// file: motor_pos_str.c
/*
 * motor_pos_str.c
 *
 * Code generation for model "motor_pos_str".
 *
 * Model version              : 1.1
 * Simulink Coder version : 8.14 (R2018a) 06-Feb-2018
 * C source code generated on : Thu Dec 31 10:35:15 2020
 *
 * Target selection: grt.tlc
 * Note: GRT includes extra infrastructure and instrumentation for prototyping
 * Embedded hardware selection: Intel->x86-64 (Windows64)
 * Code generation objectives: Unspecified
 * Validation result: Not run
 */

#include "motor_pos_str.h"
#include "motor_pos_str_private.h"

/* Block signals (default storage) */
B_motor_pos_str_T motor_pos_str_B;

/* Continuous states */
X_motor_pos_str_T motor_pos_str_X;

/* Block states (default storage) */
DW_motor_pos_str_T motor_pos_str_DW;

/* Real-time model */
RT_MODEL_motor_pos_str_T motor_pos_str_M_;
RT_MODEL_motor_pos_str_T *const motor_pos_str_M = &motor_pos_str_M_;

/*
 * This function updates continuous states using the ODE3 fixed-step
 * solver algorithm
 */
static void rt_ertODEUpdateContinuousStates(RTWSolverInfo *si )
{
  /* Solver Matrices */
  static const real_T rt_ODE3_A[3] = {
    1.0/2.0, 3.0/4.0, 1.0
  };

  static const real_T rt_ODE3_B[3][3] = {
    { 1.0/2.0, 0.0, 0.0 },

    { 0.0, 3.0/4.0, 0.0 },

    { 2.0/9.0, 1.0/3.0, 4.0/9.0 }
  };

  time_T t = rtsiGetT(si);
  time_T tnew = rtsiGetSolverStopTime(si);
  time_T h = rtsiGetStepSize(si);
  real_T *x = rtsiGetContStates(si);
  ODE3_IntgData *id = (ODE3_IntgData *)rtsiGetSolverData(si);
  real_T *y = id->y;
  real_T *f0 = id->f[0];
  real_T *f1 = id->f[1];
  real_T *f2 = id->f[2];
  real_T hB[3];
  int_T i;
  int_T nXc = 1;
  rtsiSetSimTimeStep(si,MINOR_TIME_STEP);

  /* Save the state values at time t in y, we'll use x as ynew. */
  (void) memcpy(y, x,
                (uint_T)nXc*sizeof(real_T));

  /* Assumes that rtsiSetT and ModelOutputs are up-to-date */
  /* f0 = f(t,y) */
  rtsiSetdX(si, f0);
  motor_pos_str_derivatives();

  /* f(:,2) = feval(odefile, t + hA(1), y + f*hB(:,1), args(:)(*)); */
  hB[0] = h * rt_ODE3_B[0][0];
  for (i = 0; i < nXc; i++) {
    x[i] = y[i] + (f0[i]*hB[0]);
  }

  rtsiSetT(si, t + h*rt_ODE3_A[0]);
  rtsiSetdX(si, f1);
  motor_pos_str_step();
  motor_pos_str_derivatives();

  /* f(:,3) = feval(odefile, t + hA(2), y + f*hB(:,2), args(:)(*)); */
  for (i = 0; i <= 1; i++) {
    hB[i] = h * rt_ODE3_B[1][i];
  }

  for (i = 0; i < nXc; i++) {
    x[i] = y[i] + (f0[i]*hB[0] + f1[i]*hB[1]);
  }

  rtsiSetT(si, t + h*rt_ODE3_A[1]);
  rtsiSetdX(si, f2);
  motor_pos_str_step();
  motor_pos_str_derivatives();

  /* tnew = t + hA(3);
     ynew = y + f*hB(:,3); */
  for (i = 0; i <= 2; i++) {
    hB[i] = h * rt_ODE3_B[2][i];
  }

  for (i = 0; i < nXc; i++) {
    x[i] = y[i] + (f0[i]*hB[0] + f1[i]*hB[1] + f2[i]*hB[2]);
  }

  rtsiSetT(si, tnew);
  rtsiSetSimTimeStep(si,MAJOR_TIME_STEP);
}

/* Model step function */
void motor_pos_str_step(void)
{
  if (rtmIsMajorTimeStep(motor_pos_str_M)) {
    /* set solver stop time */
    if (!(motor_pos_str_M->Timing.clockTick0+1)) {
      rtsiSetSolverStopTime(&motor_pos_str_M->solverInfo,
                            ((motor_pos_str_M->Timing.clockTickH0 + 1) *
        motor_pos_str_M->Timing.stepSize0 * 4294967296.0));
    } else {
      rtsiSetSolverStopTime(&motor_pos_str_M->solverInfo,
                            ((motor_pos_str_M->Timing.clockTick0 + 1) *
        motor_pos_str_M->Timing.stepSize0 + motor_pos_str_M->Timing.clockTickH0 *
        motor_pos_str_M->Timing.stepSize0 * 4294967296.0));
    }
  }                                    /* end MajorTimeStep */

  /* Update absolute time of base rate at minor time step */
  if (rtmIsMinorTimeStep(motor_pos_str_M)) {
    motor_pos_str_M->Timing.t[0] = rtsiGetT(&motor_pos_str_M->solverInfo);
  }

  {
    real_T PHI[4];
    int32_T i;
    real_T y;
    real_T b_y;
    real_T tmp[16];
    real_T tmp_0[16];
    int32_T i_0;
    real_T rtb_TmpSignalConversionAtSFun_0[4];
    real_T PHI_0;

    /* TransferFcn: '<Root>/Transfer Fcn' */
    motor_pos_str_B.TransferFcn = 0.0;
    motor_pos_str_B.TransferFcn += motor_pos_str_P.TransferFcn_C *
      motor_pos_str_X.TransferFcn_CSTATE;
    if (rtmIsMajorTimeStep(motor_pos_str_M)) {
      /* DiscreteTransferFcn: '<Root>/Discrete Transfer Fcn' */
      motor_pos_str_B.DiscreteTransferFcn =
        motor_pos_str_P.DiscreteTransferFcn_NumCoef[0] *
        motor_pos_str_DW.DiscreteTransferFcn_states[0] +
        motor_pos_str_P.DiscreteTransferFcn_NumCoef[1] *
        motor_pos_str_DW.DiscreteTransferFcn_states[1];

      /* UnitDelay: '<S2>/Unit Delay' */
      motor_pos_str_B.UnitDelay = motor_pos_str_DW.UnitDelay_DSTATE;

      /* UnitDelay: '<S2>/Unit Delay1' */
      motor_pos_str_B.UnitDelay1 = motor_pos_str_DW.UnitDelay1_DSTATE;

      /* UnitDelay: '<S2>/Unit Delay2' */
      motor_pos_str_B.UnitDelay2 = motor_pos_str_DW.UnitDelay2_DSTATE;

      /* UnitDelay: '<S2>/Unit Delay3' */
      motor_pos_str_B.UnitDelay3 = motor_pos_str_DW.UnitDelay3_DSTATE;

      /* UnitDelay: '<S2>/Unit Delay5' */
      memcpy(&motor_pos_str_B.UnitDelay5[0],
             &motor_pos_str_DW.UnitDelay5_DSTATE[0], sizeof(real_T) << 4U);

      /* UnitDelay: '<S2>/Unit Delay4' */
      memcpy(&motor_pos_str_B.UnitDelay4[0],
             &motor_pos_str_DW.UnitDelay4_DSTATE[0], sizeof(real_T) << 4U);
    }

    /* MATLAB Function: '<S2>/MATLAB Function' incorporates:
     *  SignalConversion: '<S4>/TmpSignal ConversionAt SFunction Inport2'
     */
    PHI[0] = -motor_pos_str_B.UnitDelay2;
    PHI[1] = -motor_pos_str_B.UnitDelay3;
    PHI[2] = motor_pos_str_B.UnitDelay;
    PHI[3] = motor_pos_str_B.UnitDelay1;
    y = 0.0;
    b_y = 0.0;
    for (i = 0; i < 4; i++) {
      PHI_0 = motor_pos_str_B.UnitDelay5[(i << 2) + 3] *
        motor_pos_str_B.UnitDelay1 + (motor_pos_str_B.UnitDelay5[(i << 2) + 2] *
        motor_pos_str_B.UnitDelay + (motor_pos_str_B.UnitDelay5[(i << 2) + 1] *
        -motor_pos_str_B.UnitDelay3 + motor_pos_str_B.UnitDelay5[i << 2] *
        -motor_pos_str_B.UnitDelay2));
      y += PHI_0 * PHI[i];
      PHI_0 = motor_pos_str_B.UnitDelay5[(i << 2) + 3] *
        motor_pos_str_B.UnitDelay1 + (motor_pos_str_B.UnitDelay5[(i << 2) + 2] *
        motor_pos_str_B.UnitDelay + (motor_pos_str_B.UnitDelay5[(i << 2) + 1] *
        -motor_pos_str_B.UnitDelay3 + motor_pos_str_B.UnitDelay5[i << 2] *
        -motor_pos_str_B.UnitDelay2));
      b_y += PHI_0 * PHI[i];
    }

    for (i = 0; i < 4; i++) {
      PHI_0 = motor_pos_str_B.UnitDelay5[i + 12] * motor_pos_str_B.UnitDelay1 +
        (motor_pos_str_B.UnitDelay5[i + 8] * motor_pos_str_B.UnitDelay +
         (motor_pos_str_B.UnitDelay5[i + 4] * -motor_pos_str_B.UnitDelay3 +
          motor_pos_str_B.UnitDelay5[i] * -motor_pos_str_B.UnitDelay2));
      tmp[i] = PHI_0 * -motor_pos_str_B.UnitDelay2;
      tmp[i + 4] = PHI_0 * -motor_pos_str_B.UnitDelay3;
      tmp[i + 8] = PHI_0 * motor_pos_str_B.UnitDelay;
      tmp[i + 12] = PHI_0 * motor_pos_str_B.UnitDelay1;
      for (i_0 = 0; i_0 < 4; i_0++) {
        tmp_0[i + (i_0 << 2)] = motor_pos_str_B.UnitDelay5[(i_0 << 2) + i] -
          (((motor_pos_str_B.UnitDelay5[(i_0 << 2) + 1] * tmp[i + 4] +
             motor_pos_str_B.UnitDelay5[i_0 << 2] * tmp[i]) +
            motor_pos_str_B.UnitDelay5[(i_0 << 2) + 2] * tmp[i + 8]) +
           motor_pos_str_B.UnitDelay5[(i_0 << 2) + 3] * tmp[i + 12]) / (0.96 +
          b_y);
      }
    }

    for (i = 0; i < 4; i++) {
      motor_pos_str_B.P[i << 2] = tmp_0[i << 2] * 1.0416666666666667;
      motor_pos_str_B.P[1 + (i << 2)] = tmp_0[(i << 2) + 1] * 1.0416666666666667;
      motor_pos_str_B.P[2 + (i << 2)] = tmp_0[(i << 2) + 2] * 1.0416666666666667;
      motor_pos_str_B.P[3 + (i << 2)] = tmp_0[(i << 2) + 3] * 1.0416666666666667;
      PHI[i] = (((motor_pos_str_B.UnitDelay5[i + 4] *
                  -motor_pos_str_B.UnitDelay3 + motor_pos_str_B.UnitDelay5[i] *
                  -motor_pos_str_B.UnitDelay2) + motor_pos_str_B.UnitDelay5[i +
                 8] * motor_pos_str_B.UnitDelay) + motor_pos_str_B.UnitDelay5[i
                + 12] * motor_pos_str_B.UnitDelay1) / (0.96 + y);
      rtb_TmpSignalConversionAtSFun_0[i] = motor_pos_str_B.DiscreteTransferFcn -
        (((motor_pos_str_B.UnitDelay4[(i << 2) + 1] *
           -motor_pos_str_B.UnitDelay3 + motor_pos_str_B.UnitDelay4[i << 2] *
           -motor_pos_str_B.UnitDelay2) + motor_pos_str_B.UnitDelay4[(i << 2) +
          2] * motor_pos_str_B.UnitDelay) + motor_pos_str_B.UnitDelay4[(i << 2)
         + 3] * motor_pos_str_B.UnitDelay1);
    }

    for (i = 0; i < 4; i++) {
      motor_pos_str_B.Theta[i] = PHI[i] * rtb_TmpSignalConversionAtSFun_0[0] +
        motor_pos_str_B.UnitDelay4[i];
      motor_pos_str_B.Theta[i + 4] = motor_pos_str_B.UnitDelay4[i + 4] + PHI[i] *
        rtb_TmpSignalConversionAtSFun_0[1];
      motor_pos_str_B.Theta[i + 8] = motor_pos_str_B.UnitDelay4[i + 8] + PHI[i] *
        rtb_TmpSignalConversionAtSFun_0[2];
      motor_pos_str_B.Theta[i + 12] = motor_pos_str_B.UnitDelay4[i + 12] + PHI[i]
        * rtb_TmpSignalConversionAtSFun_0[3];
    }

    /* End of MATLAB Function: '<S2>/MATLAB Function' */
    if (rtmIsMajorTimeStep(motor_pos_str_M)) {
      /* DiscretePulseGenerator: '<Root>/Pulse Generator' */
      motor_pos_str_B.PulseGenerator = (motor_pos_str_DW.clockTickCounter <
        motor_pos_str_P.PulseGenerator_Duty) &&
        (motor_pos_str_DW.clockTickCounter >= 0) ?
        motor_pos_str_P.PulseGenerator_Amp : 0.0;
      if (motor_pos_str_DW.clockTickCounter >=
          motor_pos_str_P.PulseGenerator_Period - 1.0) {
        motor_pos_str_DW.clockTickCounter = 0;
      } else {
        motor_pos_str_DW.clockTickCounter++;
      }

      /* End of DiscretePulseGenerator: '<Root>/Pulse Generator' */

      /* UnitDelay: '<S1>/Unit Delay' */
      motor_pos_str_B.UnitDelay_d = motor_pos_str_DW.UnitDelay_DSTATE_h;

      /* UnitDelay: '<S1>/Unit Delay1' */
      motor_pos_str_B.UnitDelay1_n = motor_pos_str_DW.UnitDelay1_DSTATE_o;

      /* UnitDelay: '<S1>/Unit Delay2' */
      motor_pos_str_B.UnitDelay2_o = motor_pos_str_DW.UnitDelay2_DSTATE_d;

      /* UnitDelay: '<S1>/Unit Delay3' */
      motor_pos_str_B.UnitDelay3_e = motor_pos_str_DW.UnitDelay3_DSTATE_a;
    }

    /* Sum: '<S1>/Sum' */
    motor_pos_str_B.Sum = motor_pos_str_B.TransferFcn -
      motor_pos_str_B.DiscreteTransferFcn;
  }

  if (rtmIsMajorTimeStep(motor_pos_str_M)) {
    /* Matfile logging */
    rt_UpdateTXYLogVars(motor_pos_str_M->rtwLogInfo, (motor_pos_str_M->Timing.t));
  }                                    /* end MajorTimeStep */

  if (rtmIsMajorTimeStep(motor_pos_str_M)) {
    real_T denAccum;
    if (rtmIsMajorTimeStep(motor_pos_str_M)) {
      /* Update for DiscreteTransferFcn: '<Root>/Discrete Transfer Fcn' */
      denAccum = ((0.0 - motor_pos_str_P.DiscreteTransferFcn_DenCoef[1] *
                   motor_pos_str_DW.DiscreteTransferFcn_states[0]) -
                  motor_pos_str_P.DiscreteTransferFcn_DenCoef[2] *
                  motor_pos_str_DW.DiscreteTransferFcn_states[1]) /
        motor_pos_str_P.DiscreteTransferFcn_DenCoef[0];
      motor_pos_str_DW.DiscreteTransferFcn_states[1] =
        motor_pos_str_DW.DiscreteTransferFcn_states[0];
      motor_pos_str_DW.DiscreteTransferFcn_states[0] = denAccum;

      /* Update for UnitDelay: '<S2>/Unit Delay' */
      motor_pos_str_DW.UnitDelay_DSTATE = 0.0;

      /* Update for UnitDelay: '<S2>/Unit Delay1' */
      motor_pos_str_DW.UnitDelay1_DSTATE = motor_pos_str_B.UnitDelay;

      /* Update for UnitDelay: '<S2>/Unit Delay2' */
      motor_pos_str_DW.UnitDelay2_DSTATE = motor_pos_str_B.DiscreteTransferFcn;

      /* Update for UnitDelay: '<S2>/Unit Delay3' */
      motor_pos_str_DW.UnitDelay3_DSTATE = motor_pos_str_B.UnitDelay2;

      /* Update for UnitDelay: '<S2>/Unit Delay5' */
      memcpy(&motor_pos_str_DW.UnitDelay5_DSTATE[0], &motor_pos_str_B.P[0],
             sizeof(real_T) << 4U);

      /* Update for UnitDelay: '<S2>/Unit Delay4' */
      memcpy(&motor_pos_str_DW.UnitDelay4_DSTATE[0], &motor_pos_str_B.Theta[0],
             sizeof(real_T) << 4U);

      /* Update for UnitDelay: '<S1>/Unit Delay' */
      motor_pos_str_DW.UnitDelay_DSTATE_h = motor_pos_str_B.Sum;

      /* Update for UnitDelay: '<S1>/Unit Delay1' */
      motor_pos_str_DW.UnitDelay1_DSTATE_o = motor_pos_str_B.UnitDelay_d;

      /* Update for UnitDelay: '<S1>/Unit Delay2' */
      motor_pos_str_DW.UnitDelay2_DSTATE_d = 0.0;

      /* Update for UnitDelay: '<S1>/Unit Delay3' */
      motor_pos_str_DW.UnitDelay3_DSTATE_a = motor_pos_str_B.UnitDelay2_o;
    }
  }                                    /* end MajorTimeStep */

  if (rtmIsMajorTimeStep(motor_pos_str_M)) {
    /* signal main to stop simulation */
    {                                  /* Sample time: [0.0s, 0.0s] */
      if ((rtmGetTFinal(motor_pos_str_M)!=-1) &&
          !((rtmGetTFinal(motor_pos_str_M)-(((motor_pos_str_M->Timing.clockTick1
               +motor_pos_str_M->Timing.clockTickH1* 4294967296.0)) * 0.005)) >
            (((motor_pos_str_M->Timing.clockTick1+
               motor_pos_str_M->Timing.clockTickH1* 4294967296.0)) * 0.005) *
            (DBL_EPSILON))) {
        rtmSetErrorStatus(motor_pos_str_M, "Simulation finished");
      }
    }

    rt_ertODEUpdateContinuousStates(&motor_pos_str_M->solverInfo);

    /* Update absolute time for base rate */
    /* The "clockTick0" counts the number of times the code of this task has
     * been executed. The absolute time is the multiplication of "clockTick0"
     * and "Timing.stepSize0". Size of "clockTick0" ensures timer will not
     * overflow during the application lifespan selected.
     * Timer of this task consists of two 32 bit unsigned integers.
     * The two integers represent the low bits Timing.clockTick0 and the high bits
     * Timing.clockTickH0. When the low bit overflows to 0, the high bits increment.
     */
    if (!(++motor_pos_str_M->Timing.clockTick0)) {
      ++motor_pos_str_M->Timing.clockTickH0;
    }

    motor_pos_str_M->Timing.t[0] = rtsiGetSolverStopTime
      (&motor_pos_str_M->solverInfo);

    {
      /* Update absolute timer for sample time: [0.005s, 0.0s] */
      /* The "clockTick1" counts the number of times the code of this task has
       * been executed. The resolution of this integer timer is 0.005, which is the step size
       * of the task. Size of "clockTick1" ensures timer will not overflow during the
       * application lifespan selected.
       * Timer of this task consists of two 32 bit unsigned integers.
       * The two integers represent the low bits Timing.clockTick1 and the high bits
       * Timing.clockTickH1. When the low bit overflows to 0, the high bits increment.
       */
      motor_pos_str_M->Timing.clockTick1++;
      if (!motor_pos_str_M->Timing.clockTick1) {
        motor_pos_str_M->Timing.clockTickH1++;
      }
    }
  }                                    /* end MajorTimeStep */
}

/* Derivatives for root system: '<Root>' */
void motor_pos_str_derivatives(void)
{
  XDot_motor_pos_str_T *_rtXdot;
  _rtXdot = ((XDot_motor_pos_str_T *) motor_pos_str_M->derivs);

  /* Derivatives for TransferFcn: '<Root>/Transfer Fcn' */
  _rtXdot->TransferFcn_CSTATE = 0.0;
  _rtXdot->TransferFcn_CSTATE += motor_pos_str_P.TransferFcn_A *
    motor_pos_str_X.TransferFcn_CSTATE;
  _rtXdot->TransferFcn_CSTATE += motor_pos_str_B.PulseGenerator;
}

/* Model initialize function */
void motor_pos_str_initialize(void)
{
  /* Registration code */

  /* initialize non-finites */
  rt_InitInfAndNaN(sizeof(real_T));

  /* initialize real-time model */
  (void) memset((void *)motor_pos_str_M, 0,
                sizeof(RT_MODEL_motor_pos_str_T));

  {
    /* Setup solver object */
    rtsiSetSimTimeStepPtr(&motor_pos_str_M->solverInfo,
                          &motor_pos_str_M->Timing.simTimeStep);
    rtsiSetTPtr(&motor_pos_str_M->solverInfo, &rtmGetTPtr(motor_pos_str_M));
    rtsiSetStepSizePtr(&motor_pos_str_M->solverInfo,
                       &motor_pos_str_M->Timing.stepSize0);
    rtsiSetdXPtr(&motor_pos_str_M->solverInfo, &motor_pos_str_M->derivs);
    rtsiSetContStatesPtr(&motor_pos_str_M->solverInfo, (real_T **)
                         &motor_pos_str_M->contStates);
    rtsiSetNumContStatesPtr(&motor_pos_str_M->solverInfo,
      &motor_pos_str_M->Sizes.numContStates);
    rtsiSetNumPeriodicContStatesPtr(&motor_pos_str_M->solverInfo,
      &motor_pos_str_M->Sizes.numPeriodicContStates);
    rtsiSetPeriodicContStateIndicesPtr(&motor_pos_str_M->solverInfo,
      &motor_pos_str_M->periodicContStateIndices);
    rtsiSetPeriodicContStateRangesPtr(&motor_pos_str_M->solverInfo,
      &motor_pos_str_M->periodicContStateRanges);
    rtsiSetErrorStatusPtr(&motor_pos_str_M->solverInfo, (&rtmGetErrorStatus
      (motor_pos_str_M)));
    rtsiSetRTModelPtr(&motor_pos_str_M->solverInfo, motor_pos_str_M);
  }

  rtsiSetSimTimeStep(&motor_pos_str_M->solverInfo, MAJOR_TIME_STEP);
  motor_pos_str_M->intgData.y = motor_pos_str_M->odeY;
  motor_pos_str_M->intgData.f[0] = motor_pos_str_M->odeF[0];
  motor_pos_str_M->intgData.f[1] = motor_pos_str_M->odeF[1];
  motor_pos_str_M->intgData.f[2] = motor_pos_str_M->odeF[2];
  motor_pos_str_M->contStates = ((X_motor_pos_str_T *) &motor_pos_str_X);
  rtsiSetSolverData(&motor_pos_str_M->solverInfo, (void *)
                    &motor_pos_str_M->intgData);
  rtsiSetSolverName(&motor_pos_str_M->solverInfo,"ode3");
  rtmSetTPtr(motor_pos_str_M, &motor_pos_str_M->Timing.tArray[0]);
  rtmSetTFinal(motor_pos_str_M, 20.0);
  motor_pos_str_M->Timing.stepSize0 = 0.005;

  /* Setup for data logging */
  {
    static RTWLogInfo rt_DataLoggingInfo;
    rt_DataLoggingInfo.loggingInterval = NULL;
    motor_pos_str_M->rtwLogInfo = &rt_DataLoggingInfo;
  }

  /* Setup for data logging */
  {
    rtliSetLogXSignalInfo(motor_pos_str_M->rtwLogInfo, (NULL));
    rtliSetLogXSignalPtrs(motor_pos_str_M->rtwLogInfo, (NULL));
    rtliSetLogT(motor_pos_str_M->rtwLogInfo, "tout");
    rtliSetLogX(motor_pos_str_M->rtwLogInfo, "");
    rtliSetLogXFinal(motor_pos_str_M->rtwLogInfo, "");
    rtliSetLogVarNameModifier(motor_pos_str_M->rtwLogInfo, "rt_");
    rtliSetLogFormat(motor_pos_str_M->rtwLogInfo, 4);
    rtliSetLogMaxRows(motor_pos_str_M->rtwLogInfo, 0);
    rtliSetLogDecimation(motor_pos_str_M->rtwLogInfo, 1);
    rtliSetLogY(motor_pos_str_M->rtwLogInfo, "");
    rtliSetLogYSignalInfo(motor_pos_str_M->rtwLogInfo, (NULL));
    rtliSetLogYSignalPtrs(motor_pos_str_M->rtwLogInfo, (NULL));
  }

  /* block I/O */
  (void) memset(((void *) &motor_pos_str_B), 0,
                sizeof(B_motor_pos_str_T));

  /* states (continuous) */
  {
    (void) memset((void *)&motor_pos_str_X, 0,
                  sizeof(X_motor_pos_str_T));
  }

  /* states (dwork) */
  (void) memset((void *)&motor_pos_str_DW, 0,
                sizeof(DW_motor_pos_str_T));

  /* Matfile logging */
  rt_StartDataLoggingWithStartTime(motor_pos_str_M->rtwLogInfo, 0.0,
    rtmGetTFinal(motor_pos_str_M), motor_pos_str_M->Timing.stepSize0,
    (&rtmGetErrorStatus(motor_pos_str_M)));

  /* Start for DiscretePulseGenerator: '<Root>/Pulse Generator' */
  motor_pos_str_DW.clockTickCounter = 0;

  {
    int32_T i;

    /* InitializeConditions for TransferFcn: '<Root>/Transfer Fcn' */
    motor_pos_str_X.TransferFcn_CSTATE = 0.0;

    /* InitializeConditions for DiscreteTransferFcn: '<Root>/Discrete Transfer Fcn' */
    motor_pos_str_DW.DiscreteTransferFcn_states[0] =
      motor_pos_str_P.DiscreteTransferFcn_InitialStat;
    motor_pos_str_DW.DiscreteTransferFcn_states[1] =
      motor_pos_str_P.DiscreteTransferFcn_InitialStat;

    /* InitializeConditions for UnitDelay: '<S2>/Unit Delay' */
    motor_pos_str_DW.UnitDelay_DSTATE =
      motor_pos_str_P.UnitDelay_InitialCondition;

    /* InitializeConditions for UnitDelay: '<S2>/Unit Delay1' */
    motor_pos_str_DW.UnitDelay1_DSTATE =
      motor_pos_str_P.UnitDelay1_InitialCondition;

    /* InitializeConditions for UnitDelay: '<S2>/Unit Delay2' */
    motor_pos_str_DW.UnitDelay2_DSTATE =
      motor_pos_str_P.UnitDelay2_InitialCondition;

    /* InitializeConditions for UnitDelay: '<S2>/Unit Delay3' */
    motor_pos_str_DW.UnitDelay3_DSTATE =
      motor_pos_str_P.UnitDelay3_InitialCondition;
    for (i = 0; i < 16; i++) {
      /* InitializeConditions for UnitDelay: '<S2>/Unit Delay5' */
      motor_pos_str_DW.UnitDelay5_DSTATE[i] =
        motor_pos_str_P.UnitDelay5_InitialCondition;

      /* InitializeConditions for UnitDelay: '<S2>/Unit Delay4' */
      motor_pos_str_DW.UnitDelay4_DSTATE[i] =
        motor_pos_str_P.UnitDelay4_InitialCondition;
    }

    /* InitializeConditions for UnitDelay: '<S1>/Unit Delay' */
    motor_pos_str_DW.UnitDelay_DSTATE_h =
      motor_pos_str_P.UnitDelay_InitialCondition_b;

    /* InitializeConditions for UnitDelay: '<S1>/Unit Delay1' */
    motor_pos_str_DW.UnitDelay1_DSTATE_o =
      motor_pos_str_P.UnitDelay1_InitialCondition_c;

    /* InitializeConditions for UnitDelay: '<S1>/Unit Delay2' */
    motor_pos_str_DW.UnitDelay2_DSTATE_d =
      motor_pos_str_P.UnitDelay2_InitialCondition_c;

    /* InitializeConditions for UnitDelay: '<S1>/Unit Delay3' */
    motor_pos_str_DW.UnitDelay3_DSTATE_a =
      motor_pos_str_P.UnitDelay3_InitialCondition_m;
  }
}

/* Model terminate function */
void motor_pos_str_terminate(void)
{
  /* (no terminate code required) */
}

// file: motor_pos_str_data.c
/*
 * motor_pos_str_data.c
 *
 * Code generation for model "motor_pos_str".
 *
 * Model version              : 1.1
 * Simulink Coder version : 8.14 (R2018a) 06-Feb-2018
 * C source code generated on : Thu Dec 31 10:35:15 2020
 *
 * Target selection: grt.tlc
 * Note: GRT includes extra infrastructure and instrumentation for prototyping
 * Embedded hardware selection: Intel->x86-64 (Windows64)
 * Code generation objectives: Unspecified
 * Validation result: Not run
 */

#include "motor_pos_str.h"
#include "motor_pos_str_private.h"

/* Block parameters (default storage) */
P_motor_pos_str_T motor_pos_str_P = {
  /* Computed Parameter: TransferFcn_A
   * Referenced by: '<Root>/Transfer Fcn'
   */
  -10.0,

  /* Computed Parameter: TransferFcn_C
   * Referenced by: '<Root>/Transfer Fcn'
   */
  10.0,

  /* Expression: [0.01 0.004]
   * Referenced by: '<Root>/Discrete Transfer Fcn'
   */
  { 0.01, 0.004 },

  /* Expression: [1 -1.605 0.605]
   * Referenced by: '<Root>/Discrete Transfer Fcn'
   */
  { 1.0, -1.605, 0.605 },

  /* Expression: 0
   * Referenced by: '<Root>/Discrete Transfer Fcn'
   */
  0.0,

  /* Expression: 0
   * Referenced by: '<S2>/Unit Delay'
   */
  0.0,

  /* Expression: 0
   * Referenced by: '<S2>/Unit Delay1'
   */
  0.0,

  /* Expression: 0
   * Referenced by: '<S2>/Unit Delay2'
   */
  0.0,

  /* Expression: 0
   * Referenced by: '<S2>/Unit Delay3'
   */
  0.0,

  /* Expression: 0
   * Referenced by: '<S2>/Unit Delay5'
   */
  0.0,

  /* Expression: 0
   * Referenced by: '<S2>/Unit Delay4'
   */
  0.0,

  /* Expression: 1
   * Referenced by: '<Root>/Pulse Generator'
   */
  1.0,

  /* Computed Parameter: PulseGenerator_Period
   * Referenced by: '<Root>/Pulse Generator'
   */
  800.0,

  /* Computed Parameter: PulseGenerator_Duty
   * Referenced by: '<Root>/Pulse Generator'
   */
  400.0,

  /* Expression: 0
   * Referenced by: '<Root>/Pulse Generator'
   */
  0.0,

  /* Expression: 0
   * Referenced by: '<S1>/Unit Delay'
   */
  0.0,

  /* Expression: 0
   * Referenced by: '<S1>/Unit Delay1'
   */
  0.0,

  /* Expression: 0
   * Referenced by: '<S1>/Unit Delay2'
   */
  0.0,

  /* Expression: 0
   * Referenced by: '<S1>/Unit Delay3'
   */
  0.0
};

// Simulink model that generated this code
simulink model "motor_pos_str"  (R2018a)
settings: Solver=FixedStepAuto  StartTime=0.0  StopTime=20  FixedStep=0.005  RelTol=1e-3

== system motor_pos_str ==
  Discrete Transfer Fcn : DiscreteTransferFcn  Numerator=[0.01 0.004]  Denominator=[1 -1.605 0.605]  SampleTime=0.005
  Mux : Mux  Inputs=2
  Pulse Generator : DiscretePulseGenerator  PulseType=Time based  Period=4  PulseWidth=50
  Scope : Scope
  Self-Tuning Regulator : Subsystem
  Theta : Scope
  Transfer Fcn : TransferFcn  Denominator=[0.1 1]
  identification : Subsystem
  u : Scope
  wires:
  Pulse Generator/1 -> Transfer Fcn/1
  Mux/1 -> Scope/1
  Self-Tuning Regulator/1(u) -> u/1, identification/1(uk), Discrete Transfer Fcn/1
  Transfer Fcn/1 -> Mux/1, Self-Tuning Regulator/1(wk)
  Discrete Transfer Fcn/1 -> Mux/2, identification/2(yk), Self-Tuning Regulator/2(yk)
  identification/1(Theta) -> Theta/1, Self-Tuning Regulator/3(Theta)

== system motor_pos_str/Self-Tuning Regulator ==
  wk : Inport
  yk : Inport  Port=2
  Theta : Inport  Port=3
  MATLAB Function : MATLAB Function  TreatAsAtomicUnit=on
  Mux1 : Mux  Inputs=2
  Mux2 : Mux  Inputs=3
  Sum : Sum  Inputs=|+-
  Unit Delay{,1..3} (4 alike) : UnitDelay  SampleTime=-1
  u : Outport
  wires:
  wk/1 -> Sum/1
  yk/1 -> Sum/2
  Sum/1 -> Mux2/1, Unit Delay/1
  Unit Delay/1 -> Mux2/2, Unit Delay1/1
  Unit Delay2/1 -> Mux1/1, Unit Delay3/1
  Unit Delay3/1 -> Mux1/2
  Theta/1 -> MATLAB Function/1(Theta)
  Mux1/1 -> MATLAB Function/3(u_)
  Unit Delay1/1 -> Mux2/3
  Mux2/1 -> MATLAB Function/2(e)
  MATLAB Function/1(u) -> u/1, Unit Delay2/1

== system motor_pos_str/identification ==
  uk : Inport
  yk : Inport  Port=2
  MATLAB Function : MATLAB Function  TreatAsAtomicUnit=on
  Mux : Mux  Inputs=2
  Mux1 : Mux  Inputs=3
  Unit Delay{,1..5} (6 alike) : UnitDelay  SampleTime=-1
  Theta : Outport
  wires:
  yk/1 -> Mux1/1, Unit Delay2/1
  uk/1 -> Unit Delay/1
  Unit Delay/1 -> Mux/1, Unit Delay1/1
  Unit Delay1/1 -> Mux/2
  Unit Delay3/1 -> Mux1/3
  Unit Delay2/1 -> Mux1/2, Unit Delay3/1
  MATLAB Function/2(Theta) -> Unit Delay4/1, Theta/1
  MATLAB Function/1(P) -> Unit Delay5/1
  Unit Delay4/1 -> MATLAB Function/4(Theta_)
  Unit Delay5/1 -> MATLAB Function/3(P_)
  Mux1/1 -> MATLAB Function/2(yk)
  Mux/1 -> MATLAB Function/1(uk)

== matlab function motor_pos_str/Self-Tuning Regulator/MATLAB Function ==
% Ham tinh thong so bo dieu khien theo pp dat cuc lien tuc
function u = STR_pp1(Theta,e,u_)

T0 = 0.005;
xi = 0.9;
wn = 50;

% Gan lai thong so de thuan tien viec tinh toan
a1 = Theta(1);
a2 = Theta(2);
b1 = Theta(3);
b2 = Theta(4);

% Tinh thong so bo dieu khien
if(xi<1)
d1 = -2*exp(-xi*wn*T0)*cos(wn*T0*sqrt(1-xi^2)); % xi<1
else
d1 = -2*exp(-xi*wn*T0)*cosh(wn*T0*sqrt(xi^2-1)); % xi>1
end
d2 = exp(-2*xi*wn*T0);
r1 = (b1+b2)*(a1*b1*b2-a2*b1^2-b2^2);
s1 = a2*((b1+b2)*(a1*b2-a2*b1)+b2*(b1*d2-b2*d1-b2));
q2 = s1/r1;
gama = q2*b2/a2;
q1 = a2/b2-q2*(b1/b2-a1/a2+1);
q0 = 1/b1*(d1+1-a1-gama);

% Luat dieu khien
u = q0*e(1) + q1*e(2) + q2*e(3) + (1-gama)*u_(1) + gama*u_(2);

== matlab function motor_pos_str/identification/MATLAB Function ==
function [P,Theta] = Uocluong(uk,yk,P_,Theta_)
lamda = 0.96;
PHI = [-yk(2); -yk(3); uk(1); uk(2)];
e = yk(1) - PHI'*Theta_;
L = P_*PHI / (lamda + PHI'*P_*PHI);
P = 1/lamda*(P_ - P_*PHI*PHI'*P_ /(lamda + PHI'*P_*PHI));
Theta = Theta_ + L*e;
